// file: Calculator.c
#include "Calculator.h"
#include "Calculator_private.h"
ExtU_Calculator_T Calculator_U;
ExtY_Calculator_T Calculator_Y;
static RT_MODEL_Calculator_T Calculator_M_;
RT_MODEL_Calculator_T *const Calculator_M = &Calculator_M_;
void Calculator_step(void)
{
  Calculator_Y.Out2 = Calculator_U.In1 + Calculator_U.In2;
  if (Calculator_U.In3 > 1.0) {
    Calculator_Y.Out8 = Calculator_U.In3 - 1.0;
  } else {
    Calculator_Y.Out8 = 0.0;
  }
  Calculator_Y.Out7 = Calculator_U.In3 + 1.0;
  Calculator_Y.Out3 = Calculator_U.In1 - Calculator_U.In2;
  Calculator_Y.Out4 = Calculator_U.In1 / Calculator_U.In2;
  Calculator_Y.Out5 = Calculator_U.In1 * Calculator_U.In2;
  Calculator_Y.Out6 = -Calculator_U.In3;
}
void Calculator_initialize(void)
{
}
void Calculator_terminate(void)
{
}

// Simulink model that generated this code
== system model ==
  In1 : Inport
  In2 : Inport
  In3 : Inport
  Out2 : Outport  <- 1: Sum#1
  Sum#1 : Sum  <- 1: In1, 2: In2
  Out3 : Outport  <- 1: Sum#2
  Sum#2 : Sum  Inputs=+-  <- 1: In1, 2: In2
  Out4 : Outport  <- 1: Product#1
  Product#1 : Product  Inputs=*/  <- 1: In1, 2: In2
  Out5 : Outport  <- 1: Product#2
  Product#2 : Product  <- 1: In1, 2: In2
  Out6 : Outport  <- 1: UnaryMinus#1
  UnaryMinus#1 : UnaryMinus  <- 1: In3
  Out7 : Outport  <- 1: IncrementStoredInteger#1
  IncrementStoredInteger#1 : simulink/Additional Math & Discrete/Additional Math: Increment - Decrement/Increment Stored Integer  <- 1: In3
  Out8 : Outport  <- 1: DecrementToZero#1
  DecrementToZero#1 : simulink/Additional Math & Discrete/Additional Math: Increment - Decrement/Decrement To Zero  <- 1: In3
